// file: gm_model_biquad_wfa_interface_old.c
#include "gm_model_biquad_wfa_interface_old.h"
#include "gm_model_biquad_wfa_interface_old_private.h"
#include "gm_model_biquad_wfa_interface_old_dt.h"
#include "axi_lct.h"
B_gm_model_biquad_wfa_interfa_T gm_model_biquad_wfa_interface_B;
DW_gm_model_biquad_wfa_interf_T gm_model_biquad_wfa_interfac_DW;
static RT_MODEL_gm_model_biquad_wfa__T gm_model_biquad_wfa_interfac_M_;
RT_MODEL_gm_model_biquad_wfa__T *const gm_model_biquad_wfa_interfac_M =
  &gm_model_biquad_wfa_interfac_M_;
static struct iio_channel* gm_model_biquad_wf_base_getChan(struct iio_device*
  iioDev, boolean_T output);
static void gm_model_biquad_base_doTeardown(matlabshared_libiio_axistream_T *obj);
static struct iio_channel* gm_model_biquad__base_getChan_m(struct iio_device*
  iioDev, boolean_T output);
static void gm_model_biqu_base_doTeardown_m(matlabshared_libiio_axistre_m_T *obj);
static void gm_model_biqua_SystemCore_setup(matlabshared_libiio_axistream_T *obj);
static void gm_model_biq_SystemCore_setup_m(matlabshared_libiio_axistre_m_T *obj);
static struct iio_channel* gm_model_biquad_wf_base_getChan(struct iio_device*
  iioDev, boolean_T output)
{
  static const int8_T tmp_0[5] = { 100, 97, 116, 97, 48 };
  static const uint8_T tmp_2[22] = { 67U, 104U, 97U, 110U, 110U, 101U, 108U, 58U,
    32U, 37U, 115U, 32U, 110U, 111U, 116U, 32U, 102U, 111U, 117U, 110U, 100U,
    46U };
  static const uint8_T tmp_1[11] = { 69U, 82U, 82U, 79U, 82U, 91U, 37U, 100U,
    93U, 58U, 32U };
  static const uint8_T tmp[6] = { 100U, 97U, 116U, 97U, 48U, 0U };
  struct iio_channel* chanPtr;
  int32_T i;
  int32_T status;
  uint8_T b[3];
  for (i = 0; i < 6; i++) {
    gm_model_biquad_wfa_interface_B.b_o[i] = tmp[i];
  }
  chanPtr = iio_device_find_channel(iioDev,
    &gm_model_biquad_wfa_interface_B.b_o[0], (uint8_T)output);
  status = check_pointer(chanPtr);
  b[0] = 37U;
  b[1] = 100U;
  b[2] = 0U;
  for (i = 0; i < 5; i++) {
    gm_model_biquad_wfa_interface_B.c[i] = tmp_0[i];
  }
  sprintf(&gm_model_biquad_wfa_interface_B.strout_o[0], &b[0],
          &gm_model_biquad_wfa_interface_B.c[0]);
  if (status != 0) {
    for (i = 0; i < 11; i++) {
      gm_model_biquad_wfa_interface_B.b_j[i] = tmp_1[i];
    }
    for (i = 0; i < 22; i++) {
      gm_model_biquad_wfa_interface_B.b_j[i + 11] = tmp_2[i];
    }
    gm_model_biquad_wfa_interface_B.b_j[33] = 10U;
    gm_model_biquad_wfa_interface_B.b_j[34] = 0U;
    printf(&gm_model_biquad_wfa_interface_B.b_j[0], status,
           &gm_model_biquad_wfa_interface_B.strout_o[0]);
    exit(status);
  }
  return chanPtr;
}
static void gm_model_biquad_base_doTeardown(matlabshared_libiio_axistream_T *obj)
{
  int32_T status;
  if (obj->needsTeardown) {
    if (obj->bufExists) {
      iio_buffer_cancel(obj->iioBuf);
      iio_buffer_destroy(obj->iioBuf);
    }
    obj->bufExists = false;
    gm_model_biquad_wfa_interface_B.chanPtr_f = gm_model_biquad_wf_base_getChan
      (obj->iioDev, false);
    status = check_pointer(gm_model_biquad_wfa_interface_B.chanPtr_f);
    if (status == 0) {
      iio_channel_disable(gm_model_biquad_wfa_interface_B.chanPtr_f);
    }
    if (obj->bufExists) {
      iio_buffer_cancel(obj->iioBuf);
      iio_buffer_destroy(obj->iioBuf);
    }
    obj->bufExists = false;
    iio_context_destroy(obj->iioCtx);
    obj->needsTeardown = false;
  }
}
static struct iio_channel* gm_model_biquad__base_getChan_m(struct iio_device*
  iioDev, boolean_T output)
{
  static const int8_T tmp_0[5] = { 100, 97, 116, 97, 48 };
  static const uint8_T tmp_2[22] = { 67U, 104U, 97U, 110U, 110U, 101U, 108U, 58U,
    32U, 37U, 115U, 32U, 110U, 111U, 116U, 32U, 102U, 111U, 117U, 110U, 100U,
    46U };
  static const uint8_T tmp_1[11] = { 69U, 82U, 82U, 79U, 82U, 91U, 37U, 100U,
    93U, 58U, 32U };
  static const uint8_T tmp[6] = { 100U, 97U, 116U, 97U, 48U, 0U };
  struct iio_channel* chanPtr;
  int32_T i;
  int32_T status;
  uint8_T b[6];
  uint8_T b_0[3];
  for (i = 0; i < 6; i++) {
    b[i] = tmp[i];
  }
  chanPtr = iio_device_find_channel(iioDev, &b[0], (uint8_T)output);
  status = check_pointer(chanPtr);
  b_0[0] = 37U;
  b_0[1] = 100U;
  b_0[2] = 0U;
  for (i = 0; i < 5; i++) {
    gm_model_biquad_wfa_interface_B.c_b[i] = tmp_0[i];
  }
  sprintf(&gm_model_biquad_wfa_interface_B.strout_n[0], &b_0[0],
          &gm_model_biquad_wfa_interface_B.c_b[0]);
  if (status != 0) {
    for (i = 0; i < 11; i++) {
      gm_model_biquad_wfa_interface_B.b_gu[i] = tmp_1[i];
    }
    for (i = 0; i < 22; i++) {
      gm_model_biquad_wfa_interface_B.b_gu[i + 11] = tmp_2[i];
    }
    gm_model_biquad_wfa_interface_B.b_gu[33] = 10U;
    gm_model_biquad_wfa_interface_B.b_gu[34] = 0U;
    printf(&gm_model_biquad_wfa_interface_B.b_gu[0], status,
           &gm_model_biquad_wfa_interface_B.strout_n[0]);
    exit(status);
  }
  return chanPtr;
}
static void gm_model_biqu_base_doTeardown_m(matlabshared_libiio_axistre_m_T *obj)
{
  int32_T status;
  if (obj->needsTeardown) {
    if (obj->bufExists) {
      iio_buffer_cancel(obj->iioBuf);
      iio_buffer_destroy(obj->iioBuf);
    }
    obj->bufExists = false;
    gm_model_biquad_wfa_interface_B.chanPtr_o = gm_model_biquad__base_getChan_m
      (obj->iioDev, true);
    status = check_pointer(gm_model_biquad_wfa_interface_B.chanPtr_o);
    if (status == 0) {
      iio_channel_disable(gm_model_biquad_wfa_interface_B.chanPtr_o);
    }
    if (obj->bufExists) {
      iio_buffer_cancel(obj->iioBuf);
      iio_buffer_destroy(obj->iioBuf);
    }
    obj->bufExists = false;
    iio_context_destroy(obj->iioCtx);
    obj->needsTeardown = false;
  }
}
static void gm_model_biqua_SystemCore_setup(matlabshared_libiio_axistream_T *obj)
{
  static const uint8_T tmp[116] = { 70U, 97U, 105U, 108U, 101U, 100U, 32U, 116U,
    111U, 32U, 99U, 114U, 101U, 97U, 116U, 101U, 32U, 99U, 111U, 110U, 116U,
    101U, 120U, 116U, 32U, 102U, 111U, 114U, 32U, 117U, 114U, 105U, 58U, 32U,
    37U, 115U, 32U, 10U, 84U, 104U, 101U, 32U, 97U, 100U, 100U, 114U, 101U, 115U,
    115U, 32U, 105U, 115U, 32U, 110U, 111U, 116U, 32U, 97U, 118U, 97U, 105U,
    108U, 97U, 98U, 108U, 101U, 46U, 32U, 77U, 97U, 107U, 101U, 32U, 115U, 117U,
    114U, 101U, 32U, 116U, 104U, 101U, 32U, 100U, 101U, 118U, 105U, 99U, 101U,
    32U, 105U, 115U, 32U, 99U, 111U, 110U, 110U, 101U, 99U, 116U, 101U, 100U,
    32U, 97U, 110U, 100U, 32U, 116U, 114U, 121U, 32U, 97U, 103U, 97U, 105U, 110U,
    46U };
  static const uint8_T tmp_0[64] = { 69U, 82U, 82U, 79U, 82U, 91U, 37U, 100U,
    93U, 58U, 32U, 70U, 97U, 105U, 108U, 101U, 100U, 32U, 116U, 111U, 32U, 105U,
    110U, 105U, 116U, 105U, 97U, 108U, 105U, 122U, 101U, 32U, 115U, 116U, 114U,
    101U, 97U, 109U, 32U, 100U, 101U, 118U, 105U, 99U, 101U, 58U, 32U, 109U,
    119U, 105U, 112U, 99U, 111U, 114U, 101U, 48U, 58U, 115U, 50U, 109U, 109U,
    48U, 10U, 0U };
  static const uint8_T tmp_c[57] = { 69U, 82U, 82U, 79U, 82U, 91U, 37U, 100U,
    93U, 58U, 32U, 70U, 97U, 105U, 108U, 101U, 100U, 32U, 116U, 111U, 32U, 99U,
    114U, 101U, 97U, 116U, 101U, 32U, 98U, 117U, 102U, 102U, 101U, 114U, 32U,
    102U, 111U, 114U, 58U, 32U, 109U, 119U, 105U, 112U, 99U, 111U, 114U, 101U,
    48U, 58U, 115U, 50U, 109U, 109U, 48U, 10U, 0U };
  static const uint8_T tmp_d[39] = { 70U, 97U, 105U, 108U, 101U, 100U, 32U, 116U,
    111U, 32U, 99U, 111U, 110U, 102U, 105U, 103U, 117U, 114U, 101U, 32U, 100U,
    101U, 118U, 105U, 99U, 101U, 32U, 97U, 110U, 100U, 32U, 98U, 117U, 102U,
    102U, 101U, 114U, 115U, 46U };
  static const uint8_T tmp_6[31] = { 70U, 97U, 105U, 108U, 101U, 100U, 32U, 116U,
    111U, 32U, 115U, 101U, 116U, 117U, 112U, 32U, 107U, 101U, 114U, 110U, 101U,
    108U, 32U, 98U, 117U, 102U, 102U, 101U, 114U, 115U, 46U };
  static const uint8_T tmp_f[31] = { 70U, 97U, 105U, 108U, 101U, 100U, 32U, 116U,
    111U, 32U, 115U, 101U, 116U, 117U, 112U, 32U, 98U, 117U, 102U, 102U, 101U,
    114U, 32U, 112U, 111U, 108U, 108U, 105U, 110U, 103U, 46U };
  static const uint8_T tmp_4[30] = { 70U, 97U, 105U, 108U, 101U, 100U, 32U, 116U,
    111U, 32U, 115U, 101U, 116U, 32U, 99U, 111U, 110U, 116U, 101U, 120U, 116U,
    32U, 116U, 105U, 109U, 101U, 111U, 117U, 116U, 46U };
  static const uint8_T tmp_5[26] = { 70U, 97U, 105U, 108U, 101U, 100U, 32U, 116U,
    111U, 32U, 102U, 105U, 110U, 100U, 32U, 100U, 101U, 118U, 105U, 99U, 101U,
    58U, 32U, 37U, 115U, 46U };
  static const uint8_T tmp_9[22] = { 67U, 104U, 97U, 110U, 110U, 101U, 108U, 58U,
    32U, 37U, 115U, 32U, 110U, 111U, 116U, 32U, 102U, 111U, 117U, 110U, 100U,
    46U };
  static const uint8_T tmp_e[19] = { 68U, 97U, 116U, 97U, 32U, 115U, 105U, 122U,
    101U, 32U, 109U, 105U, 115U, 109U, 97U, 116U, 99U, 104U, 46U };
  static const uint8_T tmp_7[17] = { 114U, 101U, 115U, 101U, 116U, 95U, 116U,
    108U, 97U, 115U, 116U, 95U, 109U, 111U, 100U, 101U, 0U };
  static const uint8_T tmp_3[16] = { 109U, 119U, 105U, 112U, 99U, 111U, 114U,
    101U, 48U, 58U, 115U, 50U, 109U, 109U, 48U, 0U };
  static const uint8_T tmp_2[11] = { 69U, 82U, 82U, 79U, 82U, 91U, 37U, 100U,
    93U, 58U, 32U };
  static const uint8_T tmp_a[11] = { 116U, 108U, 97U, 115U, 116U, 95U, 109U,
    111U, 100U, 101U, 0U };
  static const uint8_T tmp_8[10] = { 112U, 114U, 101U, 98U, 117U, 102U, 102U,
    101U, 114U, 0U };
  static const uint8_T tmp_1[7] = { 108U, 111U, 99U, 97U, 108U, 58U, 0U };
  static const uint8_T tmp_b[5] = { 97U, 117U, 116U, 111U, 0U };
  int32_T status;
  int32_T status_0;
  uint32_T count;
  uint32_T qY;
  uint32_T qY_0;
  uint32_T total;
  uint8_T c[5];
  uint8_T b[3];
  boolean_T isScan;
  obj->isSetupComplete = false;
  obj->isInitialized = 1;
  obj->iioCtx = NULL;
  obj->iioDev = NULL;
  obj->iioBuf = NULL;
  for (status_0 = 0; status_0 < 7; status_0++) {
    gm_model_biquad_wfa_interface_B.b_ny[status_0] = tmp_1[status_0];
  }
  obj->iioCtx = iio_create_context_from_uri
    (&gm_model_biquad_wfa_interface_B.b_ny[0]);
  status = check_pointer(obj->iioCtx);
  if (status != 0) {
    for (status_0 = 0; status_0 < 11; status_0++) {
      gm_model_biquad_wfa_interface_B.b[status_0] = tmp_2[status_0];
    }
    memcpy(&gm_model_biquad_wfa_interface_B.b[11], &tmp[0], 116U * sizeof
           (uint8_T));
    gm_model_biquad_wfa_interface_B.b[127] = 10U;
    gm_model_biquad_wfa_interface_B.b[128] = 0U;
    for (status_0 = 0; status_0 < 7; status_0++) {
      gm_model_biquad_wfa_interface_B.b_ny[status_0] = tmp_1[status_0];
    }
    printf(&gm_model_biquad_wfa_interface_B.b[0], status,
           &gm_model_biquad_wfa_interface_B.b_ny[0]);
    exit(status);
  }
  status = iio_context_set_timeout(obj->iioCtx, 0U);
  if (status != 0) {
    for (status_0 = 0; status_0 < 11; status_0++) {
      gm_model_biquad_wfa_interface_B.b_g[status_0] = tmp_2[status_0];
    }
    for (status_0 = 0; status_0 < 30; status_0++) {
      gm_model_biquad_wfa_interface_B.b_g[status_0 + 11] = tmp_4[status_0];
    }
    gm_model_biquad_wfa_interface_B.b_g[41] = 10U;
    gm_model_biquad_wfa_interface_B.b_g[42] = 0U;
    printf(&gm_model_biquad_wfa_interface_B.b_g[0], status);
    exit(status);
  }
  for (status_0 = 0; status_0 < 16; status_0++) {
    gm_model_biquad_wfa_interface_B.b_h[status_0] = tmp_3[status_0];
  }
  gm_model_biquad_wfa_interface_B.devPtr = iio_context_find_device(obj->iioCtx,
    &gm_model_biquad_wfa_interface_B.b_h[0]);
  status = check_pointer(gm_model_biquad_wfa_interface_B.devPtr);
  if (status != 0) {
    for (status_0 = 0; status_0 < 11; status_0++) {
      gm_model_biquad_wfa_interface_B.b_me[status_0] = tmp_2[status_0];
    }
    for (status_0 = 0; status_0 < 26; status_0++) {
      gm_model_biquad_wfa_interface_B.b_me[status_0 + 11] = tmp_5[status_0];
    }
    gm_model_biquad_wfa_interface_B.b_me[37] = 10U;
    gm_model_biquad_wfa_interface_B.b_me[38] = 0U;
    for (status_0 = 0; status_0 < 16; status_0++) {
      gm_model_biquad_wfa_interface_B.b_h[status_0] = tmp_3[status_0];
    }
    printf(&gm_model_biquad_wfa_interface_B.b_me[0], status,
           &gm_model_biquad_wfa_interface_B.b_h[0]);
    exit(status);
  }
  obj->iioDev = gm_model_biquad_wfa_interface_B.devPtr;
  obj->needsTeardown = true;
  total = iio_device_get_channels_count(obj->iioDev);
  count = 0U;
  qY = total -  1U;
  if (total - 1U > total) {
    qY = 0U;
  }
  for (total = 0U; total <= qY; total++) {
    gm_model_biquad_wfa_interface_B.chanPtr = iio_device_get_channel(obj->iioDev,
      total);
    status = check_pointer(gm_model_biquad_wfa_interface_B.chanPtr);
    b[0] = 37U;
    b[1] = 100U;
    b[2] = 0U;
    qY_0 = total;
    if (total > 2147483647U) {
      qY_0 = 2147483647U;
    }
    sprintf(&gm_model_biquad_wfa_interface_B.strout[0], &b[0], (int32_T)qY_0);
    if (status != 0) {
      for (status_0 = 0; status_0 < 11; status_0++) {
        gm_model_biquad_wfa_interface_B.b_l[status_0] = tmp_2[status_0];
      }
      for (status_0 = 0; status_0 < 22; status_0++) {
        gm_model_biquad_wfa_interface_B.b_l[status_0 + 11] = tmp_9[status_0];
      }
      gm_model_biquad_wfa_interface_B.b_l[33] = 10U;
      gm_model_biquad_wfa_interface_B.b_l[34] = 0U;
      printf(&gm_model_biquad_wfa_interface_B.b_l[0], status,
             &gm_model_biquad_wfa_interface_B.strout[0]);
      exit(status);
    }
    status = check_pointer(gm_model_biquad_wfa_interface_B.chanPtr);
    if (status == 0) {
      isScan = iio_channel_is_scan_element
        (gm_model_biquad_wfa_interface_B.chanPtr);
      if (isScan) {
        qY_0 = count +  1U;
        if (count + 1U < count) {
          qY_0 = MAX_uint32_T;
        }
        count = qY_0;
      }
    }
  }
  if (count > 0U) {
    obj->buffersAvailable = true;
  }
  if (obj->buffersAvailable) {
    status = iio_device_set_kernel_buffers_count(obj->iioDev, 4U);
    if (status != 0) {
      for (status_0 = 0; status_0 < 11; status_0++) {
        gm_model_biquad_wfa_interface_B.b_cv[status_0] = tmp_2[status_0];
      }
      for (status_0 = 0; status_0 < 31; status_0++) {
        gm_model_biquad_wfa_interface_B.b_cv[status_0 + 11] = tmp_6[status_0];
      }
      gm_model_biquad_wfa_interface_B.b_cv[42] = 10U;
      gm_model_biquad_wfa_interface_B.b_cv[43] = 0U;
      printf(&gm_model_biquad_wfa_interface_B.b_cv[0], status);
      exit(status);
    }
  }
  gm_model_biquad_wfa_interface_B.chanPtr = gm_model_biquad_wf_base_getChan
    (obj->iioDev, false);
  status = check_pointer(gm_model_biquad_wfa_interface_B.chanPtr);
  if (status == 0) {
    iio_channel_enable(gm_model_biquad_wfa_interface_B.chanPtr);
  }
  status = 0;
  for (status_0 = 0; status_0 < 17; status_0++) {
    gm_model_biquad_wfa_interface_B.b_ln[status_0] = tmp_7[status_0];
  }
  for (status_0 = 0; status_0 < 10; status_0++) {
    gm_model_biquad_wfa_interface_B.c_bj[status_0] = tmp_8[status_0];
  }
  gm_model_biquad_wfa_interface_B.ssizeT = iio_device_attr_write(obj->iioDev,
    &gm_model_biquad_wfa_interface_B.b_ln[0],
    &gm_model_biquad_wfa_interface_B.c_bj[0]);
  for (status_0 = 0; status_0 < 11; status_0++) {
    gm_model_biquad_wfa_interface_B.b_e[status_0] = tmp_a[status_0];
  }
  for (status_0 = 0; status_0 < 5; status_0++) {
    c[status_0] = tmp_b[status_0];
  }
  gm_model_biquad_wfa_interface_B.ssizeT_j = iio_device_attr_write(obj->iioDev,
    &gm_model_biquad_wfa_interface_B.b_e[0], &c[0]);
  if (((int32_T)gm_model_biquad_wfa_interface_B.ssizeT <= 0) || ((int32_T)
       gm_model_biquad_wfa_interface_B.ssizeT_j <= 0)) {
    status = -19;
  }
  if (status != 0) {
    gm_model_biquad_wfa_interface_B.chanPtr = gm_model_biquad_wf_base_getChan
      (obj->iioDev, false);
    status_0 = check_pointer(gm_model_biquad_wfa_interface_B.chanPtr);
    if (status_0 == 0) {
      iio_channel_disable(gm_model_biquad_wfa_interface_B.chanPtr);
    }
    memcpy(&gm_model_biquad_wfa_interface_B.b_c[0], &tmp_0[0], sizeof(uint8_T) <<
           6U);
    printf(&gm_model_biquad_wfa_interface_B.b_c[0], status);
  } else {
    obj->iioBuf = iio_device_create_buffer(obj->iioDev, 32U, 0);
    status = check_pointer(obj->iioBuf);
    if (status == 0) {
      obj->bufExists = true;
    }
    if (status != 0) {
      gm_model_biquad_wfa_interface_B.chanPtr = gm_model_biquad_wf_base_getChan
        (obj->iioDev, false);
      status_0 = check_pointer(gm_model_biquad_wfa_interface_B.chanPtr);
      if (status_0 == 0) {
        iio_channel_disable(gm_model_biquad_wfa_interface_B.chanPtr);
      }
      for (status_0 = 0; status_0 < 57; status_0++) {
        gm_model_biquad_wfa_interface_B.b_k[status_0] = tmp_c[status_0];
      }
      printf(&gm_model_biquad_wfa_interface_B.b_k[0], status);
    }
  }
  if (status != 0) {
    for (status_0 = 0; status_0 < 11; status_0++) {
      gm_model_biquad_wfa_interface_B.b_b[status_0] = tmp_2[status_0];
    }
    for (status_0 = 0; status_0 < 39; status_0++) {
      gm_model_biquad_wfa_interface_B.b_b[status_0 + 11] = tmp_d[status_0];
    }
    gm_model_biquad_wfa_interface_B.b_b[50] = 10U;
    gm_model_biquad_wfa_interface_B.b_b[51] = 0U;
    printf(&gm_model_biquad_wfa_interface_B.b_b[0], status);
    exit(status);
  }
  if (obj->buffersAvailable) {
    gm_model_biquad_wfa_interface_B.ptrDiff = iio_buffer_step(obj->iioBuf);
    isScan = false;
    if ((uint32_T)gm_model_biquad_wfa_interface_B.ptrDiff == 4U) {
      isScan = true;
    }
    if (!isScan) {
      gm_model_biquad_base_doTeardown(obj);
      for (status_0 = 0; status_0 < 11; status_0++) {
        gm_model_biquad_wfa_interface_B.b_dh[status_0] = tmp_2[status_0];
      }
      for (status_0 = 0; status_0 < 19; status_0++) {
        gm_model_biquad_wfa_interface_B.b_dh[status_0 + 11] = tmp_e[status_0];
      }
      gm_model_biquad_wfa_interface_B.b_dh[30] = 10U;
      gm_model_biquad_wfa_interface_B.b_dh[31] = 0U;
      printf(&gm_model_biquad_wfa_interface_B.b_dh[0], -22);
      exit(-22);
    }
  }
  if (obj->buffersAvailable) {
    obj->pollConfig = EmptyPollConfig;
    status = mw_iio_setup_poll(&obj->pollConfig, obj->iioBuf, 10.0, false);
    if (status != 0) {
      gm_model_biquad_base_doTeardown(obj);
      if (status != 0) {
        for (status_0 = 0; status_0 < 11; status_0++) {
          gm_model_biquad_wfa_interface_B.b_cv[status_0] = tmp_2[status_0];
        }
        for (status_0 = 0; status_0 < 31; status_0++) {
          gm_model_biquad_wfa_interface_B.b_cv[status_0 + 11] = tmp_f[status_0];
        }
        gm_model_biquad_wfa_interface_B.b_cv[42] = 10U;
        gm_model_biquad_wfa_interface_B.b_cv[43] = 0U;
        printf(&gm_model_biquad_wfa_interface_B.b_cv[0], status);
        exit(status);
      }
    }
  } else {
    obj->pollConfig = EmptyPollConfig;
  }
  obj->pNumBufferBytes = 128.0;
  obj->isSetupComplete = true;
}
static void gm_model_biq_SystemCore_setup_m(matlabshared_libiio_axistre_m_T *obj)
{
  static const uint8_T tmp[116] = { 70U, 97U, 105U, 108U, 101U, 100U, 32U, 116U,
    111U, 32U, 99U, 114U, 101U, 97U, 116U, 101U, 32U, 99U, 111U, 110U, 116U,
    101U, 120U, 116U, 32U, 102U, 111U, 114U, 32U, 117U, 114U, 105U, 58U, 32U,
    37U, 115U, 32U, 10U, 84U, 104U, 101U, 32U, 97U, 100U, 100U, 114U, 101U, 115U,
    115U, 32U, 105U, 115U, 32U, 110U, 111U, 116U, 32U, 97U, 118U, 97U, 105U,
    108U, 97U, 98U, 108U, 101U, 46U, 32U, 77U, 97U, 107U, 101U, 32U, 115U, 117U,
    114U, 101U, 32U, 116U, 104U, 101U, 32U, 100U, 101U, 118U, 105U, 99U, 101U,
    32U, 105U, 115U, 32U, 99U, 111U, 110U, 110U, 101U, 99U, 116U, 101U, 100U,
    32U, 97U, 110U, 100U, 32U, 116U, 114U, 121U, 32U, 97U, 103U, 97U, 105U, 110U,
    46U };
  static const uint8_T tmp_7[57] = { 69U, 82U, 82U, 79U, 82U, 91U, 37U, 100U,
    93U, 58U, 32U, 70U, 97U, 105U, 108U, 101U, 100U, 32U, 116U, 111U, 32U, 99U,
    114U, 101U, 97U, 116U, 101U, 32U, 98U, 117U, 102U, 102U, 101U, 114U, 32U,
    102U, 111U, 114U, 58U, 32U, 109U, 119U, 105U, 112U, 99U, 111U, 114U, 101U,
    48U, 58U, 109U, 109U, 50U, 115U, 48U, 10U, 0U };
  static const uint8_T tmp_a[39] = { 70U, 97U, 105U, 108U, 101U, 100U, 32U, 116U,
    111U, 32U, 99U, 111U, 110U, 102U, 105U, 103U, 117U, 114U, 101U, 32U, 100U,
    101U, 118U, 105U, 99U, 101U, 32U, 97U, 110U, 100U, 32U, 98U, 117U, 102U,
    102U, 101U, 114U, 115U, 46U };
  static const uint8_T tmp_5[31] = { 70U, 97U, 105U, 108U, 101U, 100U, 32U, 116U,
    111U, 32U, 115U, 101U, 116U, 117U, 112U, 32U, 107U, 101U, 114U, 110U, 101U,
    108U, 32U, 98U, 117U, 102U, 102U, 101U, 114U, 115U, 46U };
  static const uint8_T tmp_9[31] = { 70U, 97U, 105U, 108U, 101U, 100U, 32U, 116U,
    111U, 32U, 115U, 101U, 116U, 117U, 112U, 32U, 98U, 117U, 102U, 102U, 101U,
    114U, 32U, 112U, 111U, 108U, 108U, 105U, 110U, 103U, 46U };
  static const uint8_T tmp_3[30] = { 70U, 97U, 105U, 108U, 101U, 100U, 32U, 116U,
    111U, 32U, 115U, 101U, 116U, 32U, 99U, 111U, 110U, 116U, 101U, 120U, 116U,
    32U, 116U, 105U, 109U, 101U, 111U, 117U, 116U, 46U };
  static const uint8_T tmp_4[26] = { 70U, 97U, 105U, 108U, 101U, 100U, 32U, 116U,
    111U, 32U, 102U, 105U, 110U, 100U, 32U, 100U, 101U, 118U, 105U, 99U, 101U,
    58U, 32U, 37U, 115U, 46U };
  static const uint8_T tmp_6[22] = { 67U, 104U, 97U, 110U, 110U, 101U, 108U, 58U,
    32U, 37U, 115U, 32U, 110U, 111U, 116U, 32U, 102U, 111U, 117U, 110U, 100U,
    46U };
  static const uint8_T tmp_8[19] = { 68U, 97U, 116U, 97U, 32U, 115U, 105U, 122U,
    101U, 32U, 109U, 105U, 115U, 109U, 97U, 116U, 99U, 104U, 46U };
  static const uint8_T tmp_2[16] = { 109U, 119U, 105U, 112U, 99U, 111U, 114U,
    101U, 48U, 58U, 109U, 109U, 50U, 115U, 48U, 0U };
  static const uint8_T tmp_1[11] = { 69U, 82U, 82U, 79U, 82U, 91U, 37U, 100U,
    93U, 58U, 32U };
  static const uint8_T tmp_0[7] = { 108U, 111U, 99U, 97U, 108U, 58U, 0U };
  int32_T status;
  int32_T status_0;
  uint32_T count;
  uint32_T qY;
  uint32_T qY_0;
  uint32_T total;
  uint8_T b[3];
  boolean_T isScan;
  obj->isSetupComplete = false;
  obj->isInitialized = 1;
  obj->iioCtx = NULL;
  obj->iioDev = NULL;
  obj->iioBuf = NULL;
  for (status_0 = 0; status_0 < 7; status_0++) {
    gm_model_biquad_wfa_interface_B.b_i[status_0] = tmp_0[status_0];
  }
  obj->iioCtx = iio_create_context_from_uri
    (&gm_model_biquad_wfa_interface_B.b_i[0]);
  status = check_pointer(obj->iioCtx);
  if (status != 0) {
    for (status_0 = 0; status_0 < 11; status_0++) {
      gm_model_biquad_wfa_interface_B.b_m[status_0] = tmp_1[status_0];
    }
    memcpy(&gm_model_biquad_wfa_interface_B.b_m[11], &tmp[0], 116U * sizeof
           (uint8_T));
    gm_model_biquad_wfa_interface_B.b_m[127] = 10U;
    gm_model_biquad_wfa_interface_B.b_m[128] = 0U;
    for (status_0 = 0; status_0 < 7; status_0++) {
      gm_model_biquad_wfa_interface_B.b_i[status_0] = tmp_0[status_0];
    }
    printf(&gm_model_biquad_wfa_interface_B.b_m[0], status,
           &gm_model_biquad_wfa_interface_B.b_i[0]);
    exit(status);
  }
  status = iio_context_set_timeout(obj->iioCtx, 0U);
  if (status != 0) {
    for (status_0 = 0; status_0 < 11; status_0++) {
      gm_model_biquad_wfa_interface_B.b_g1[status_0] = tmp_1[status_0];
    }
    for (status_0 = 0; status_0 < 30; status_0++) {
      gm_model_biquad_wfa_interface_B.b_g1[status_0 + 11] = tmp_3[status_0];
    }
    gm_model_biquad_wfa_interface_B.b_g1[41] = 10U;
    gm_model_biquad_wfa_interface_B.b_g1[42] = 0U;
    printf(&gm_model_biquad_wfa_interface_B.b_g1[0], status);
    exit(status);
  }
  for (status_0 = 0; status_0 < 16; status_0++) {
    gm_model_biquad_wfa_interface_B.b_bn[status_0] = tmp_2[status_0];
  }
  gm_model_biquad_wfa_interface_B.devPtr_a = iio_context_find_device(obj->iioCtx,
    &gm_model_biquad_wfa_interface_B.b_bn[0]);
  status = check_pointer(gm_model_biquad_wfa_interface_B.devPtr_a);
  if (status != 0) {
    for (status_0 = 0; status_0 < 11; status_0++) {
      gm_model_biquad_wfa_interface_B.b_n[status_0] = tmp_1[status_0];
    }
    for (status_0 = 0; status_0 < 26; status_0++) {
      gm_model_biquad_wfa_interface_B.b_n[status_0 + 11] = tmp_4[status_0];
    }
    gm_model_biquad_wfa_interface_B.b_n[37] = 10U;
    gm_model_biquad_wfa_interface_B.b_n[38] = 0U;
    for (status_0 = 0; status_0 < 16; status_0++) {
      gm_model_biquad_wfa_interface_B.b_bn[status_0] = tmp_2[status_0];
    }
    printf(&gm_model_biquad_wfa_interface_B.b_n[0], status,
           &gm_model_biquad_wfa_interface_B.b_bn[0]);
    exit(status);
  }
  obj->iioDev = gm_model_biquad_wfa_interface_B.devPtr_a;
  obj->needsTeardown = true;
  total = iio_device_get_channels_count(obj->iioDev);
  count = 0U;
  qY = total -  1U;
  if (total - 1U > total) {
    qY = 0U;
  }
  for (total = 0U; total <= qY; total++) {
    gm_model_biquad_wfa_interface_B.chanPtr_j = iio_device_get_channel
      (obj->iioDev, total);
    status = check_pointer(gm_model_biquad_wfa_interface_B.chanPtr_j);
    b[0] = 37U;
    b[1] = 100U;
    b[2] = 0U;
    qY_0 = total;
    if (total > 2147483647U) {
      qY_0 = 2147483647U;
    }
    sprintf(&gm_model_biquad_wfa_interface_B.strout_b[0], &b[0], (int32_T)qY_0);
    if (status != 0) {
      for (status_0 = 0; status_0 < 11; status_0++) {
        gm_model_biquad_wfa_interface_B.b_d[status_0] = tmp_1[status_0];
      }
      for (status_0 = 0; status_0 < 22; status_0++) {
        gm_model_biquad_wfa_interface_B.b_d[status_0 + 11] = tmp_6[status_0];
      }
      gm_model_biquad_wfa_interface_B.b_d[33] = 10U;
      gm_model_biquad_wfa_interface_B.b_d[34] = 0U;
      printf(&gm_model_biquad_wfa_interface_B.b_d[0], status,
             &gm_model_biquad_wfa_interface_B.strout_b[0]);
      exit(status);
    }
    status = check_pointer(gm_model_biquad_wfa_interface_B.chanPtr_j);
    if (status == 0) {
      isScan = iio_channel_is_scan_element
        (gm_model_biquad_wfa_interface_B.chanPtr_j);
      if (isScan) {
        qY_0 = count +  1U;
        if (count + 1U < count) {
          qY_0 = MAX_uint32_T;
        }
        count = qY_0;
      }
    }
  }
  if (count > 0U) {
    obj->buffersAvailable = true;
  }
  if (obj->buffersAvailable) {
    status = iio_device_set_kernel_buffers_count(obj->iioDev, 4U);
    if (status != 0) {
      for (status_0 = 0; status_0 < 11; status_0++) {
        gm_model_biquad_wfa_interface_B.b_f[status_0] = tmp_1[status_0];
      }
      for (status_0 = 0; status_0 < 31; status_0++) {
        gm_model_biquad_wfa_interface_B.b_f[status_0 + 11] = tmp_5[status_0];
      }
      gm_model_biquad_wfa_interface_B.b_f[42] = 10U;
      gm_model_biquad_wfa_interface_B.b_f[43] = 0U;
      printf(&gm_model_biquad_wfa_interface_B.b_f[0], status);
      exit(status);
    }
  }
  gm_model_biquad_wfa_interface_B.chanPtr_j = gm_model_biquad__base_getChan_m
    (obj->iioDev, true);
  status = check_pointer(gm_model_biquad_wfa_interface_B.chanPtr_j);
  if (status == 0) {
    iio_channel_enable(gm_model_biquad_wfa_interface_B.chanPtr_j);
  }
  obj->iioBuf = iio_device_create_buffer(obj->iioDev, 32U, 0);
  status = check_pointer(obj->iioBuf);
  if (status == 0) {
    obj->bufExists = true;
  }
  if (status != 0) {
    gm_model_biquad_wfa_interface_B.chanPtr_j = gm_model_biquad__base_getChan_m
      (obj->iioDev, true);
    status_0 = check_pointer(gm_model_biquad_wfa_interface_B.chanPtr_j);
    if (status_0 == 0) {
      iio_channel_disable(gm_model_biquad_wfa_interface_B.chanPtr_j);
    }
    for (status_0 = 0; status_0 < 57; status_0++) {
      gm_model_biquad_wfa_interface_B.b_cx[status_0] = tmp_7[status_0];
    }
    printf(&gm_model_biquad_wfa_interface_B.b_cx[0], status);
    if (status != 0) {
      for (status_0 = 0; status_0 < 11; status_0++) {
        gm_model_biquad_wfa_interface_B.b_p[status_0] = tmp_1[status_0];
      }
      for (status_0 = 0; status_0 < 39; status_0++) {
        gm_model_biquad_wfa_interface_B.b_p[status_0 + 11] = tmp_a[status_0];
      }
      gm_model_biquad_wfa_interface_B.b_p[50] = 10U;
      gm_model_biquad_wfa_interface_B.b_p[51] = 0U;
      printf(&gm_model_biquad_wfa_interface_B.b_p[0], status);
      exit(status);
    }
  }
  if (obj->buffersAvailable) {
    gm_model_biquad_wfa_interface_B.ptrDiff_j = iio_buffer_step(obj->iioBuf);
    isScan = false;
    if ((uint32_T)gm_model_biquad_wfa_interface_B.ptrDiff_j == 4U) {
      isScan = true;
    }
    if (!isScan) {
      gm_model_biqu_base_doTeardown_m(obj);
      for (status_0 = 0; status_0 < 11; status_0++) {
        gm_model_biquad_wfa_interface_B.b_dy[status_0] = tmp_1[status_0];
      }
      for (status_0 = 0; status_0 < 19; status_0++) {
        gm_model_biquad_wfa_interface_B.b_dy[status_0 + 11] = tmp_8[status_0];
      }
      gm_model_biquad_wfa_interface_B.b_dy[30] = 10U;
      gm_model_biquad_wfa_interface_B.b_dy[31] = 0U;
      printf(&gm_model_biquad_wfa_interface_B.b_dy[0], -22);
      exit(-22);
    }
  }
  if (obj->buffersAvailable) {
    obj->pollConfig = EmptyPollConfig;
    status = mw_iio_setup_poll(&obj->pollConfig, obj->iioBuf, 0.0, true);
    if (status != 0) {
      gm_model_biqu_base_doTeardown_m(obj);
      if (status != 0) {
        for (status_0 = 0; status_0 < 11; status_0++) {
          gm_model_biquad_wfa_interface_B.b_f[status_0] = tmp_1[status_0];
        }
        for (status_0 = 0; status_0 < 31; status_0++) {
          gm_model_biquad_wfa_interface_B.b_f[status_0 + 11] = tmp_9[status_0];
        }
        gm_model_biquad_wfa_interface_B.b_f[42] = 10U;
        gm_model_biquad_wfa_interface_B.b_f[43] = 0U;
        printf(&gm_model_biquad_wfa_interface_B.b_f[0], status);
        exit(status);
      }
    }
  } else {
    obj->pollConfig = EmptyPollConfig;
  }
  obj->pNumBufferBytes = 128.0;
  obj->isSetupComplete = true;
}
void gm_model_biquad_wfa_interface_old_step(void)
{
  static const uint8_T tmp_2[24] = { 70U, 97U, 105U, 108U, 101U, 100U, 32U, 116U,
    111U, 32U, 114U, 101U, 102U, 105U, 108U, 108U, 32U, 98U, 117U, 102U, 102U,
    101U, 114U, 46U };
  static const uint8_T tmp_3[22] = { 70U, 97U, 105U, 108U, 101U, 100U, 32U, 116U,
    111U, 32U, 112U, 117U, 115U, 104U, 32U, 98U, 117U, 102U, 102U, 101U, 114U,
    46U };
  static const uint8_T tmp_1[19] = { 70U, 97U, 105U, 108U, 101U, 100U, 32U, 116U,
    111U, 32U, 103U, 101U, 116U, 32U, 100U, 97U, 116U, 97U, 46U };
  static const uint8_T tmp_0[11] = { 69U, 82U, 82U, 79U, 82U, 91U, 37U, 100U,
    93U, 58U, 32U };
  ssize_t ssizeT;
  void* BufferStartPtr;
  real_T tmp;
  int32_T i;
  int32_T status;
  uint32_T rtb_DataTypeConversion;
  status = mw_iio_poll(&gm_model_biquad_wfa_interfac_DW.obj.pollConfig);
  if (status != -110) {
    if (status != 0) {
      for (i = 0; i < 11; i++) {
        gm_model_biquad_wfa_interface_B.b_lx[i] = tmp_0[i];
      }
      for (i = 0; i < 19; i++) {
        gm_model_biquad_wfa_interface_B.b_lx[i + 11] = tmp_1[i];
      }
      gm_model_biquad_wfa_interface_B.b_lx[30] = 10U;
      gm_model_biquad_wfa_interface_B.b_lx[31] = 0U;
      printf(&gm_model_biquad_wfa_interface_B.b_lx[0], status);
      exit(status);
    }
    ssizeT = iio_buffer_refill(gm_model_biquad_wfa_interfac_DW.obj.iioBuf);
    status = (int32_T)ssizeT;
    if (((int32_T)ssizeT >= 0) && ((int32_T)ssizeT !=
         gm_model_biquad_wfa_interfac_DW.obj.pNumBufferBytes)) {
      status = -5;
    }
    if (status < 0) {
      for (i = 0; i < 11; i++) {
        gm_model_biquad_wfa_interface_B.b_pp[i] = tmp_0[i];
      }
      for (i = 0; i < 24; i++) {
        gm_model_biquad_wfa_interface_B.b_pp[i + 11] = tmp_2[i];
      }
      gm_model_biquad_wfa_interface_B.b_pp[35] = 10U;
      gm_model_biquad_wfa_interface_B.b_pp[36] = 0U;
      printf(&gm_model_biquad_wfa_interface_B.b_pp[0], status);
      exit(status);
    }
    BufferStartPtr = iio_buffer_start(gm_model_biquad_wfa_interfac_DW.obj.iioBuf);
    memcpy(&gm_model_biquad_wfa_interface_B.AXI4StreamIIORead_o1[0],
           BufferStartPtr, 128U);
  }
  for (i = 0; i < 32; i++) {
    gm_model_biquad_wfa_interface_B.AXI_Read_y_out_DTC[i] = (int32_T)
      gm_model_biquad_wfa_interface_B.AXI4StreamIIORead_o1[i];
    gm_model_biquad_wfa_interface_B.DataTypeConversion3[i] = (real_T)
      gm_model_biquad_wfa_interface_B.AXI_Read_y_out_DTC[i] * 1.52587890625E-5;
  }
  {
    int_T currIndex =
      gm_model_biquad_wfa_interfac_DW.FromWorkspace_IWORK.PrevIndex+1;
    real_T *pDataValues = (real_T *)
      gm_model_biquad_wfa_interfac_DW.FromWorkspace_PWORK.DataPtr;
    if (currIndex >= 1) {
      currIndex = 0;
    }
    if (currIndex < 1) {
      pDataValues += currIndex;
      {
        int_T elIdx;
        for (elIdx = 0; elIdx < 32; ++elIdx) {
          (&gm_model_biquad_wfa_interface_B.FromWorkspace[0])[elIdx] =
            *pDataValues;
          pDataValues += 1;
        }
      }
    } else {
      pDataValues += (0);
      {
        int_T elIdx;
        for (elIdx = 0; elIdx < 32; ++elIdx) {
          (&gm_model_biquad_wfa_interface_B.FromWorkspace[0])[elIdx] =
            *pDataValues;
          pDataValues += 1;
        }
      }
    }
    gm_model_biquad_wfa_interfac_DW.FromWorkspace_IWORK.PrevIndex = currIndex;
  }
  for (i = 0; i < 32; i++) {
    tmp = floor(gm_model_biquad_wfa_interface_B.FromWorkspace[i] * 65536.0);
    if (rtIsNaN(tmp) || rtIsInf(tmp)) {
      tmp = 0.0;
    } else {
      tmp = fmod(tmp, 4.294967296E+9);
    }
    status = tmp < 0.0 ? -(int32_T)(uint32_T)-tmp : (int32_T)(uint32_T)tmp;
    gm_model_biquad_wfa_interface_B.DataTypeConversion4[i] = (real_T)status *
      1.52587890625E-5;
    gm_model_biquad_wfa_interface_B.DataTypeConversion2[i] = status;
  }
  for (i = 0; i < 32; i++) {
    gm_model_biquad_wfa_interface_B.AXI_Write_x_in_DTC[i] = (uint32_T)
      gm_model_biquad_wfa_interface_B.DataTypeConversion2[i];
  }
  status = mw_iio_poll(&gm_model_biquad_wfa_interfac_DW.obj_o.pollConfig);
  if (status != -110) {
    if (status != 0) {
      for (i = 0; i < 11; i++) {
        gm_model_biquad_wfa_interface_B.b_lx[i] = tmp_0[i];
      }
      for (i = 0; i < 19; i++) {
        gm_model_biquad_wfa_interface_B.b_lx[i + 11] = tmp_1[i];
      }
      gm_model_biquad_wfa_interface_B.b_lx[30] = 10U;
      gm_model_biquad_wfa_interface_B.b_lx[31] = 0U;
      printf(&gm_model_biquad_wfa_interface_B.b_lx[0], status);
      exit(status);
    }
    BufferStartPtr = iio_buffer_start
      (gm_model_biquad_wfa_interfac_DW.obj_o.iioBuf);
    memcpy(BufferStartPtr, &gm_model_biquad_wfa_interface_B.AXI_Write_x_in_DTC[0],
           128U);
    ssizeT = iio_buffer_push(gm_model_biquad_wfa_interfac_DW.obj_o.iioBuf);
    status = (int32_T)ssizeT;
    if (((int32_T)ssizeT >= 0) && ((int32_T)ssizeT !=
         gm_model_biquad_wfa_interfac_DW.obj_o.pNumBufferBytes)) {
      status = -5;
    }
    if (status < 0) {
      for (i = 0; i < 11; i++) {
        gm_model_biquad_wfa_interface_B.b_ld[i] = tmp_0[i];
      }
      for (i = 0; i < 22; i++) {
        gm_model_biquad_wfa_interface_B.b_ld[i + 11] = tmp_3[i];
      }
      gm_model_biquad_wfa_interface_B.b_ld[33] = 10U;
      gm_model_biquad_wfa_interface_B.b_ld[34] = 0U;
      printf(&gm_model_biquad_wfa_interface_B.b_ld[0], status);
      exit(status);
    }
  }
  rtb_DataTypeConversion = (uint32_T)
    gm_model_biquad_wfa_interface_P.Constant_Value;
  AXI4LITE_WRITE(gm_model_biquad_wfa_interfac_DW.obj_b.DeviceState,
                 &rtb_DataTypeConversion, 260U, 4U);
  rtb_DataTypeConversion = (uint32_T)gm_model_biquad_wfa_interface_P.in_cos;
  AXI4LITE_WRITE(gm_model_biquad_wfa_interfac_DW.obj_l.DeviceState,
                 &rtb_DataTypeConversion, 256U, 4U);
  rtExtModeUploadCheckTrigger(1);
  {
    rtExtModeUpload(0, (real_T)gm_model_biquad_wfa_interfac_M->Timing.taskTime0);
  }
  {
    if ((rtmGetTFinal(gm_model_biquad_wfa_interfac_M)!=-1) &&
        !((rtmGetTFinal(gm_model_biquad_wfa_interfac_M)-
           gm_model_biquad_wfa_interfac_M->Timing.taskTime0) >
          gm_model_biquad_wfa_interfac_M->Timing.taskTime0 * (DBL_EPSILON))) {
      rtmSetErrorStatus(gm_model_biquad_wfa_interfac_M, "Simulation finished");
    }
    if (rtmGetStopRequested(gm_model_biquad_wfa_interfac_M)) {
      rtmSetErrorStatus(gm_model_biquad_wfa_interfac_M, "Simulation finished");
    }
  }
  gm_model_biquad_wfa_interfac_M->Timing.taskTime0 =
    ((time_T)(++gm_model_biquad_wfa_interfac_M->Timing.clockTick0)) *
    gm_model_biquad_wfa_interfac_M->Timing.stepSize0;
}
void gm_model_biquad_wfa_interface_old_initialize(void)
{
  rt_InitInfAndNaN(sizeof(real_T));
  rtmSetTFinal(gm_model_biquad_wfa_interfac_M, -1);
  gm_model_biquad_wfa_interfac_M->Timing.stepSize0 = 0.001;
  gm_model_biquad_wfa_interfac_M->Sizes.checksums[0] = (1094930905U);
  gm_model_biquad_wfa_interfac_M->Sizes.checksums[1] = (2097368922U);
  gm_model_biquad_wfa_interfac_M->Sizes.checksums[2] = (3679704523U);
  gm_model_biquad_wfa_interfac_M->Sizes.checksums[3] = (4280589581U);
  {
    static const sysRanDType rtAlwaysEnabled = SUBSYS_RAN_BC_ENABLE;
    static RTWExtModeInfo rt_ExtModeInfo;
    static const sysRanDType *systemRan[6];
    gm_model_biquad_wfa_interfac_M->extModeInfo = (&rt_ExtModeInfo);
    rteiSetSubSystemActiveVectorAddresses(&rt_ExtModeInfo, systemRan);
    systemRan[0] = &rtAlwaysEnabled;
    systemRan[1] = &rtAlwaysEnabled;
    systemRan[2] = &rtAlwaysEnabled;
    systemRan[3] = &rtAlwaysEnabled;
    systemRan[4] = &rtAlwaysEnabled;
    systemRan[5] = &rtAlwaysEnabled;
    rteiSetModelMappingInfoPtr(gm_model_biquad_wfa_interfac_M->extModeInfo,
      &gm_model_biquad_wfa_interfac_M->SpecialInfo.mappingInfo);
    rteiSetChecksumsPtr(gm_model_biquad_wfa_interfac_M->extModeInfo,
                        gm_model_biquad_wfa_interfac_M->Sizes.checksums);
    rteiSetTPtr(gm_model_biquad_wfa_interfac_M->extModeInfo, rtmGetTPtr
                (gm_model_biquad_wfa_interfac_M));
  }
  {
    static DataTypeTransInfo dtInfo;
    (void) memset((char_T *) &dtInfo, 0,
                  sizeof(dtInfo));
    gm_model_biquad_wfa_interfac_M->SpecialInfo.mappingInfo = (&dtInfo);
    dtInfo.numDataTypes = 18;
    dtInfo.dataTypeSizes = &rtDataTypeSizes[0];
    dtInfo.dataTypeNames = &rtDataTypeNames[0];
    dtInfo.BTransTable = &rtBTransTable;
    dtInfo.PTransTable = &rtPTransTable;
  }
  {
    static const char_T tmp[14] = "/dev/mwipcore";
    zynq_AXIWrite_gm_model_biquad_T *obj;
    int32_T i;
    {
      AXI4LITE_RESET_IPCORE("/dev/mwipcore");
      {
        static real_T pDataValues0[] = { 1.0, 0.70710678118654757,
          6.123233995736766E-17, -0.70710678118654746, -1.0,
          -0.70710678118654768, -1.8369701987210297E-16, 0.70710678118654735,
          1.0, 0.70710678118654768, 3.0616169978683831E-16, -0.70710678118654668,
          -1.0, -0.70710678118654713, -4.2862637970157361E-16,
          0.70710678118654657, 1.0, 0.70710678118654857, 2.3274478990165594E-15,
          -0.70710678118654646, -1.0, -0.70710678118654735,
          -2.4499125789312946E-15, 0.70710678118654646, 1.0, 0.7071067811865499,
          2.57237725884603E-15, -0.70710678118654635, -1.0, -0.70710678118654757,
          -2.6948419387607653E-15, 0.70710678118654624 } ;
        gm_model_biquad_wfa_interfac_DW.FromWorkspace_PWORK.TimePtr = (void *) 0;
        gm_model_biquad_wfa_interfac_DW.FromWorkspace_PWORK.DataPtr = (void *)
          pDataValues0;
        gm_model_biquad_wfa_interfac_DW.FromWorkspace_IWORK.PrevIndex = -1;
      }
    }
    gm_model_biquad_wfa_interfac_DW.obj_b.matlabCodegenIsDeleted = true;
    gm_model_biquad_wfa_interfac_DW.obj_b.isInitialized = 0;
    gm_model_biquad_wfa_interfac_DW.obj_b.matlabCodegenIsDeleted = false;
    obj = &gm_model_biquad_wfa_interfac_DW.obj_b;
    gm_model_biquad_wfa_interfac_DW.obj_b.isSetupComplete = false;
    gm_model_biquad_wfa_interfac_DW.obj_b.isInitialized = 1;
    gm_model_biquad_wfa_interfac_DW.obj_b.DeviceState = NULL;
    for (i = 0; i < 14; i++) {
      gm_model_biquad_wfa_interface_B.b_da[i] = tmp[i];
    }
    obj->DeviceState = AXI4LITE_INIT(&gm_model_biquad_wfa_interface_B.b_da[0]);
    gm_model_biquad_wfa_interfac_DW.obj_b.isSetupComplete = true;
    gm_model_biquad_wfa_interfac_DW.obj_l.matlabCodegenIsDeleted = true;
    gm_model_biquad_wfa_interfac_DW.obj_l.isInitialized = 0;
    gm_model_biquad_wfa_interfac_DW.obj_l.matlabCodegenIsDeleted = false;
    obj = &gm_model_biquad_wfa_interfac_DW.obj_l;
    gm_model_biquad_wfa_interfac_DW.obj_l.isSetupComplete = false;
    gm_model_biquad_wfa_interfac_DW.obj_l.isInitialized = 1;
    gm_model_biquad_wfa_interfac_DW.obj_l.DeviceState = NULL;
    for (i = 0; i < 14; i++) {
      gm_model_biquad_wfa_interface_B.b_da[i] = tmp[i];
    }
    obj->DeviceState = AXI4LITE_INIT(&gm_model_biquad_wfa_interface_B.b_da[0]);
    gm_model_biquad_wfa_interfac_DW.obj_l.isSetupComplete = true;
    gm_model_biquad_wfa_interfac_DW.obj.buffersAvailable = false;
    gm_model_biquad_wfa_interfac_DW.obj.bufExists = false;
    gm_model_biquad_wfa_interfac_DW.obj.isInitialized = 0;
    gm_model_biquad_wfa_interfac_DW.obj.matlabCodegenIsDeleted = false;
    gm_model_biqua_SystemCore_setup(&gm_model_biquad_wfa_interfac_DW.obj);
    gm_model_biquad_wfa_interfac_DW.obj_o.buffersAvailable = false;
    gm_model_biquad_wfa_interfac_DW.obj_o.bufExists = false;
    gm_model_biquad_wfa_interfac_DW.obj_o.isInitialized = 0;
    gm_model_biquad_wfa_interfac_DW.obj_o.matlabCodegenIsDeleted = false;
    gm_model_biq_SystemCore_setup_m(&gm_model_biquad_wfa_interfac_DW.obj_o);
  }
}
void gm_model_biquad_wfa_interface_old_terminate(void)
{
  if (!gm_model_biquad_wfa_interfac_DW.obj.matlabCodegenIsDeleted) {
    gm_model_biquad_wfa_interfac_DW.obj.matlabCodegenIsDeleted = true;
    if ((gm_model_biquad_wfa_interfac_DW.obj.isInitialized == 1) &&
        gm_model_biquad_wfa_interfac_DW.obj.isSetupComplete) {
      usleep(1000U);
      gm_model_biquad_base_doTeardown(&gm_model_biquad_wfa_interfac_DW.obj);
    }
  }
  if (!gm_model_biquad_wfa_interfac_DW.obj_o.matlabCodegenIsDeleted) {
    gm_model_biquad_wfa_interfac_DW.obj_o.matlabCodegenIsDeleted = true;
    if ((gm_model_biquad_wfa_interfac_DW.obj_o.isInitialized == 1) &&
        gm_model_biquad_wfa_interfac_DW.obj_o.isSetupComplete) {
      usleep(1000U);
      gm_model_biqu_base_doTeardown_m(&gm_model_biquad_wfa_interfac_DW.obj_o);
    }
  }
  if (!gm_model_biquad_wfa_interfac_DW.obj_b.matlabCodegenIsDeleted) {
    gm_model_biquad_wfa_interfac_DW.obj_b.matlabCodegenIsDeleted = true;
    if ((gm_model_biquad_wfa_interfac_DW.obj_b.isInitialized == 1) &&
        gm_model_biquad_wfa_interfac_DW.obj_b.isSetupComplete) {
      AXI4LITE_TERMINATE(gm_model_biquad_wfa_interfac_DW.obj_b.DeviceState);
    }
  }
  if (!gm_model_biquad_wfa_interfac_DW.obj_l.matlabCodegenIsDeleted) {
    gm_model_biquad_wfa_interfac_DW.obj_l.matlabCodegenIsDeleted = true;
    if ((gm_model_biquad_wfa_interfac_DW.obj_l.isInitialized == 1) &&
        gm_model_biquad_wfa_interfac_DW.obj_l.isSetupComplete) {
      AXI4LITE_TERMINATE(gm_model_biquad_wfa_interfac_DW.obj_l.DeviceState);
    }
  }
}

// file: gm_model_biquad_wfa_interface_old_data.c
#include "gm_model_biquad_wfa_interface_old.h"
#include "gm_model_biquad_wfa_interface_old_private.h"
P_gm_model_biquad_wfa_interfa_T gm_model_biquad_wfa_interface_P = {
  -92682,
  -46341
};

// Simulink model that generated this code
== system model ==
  DataTypeConversion3 : DataTypeConversion  <- 1: AXI_Read_y_out_DTC
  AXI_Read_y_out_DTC : DataTypeConversion  <- 1: AXI4StreamIIORead
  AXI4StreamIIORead : axi_iio_lib/AXI4-Stream IIO Read
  DataTypeConversion4 : DataTypeConversion  <- 1: DataTypeConversion2
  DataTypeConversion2 : DataTypeConversion  <- 1: FromWorkspace
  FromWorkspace : FromWorkspace
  AXI4StreamIIOWrite#1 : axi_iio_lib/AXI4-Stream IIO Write  <- 1: AXI_Write_x_in_DTC
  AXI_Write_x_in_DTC : DataTypeConversion  <- 1: DataTypeConversion2
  DataTypeConversion : DataTypeConversion
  AXI4InterfaceWrite#1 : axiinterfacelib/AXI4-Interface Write  <- 1: DataTypeConversion#1
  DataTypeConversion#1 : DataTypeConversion  <- 1: Constant
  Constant : Constant  Value=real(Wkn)
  DataTypeConversion#2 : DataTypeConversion
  AXI4InterfaceWrite#2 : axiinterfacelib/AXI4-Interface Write  <- 1: DataTypeConversion#3
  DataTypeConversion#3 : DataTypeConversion  <- 1: Constant#1
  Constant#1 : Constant  Value=in_cos
